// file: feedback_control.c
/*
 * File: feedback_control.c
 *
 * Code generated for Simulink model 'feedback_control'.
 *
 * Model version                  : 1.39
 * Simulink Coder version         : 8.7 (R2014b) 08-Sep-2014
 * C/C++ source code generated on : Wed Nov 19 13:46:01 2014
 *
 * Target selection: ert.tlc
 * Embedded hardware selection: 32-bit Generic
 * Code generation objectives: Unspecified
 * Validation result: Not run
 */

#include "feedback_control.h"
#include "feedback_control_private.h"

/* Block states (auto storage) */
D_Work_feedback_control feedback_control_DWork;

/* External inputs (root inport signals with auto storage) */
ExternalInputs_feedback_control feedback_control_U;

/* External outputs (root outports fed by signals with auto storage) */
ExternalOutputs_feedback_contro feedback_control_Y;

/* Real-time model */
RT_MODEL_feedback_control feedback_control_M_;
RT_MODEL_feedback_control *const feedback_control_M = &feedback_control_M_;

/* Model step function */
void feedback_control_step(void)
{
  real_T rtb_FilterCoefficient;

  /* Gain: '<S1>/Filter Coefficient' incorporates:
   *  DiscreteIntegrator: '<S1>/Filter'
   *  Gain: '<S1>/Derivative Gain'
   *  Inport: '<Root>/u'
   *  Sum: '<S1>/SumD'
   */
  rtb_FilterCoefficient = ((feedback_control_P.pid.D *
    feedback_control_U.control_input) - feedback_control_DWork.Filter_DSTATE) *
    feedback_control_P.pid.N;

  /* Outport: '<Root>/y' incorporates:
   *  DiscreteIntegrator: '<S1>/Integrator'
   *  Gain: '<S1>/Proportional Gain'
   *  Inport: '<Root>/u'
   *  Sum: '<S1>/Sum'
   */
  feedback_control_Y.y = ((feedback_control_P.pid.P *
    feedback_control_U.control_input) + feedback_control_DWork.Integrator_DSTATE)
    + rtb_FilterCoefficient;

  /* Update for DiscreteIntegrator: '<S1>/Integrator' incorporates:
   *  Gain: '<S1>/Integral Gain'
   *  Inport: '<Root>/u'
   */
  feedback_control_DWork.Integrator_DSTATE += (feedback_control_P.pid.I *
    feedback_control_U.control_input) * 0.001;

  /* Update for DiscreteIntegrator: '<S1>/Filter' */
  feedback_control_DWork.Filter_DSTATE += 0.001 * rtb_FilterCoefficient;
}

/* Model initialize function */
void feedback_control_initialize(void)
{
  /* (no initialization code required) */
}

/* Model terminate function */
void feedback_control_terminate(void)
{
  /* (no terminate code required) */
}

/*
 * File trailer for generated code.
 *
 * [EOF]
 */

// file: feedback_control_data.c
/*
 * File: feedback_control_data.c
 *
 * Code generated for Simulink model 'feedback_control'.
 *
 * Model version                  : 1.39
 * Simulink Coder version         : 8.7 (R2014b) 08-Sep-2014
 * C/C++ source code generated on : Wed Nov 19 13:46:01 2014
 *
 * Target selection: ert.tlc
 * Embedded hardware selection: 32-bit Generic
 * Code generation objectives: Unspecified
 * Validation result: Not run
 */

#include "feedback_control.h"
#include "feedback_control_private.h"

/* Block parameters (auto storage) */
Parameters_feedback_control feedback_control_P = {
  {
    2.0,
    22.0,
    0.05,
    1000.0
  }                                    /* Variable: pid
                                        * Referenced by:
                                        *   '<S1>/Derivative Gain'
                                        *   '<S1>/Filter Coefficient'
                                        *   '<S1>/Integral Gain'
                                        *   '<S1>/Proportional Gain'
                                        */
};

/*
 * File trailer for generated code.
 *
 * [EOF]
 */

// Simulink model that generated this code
simulink model "feedback_control"  (R2014b)
settings: Solver=FixedStepDiscrete  StartTime=0.0  StopTime=10.0  FixedStep=T_sample_control  RelTol=1e-3
undefined symbols (not defined in the file): pid, T_sample_control
libraries: simulink x1

== system feedback_control ==
  note: Copyright 2012 The MathWorks, Inc.
  u : Inport  OutDataTypeStr=double  PortDimensions=1  SampleTime=T_sample_control
  Discrete PID Controller : simulink/Continuous/PID Controller  Controller=PID  TimeDomain=Discrete-time  SampleTime=T_sample_control  IntegratorMethod=Forward Euler  FilterMethod=Forward Euler  Form=Parallel  P=pid.P  I=pid.I  D=pid.D  N=pid.N  InitialConditionSource=internal  InitialConditionForIntegrator=0  InitialConditionForFilter=0  ExternalReset=none  LimitOutput=off  UpperSaturationLimit=inf  LowerSaturationLimit=-inf  LinearizeAsGain=off  AntiWindupMode=none  Kb=1  TrackingMode=off  Kt=1  PParamMin=[]  PParamMax=[]  IParamMin=[]  IParamMax=[]  DParamMin=[]  DParamMax=[]  NParamMin=[]  NParamMax=[]  KbParamMin=[]  KbParamMax=[]  KtParamMin=[]  KtParamMax=[]  POutMin=[]  POutMax=[]  IOutMin=[]  IOutMax=[]  DOutMin=[]  DOutMax=[]  NOutMin=[]  NOutMax=[]  KbOutMin=[]  KbOutMax=[]  KtOutMin=[]  KtOutMax=[]  IntegratorOutMin=[]  IntegratorOutMax=[]  FilterOutMin=[]  FilterOutMax=[]  SumOutMin=[]  SumOutMax=[]  SumI1OutMin=[]  SumI1OutMax=[]  SumI2OutMin=[]  SumI2OutMax=[]  SumI3OutMin=[]  SumI3OutMax=[]  SumDOutMin=[]  SumDOutMax=[]  SaturationOutMin=[]  SaturationOutMax=[]  IntegratorContinuousStateAttributes=''  IntegratorStateMustResolveToSignalObject=off  IntegratorRTWStateStorageClass=Auto  FilterContinuousStateAttributes=''  FilterStateMustResolveToSignalObject=off  FilterRTWStateStorageClass=Auto  DifferentiatorICPrevScaledInput=0  DifferentiatorOutMin=[]  DifferentiatorOutMax=[]  UseFilter=on
  y : Outport  OutDataTypeStr=double  PortDimensions=1  SampleTime=T_sample_control
  wires:
  u/1 -> Discrete PID Controller/1  "control_input"
  Discrete PID Controller/1 -> y/1  "control_output"
